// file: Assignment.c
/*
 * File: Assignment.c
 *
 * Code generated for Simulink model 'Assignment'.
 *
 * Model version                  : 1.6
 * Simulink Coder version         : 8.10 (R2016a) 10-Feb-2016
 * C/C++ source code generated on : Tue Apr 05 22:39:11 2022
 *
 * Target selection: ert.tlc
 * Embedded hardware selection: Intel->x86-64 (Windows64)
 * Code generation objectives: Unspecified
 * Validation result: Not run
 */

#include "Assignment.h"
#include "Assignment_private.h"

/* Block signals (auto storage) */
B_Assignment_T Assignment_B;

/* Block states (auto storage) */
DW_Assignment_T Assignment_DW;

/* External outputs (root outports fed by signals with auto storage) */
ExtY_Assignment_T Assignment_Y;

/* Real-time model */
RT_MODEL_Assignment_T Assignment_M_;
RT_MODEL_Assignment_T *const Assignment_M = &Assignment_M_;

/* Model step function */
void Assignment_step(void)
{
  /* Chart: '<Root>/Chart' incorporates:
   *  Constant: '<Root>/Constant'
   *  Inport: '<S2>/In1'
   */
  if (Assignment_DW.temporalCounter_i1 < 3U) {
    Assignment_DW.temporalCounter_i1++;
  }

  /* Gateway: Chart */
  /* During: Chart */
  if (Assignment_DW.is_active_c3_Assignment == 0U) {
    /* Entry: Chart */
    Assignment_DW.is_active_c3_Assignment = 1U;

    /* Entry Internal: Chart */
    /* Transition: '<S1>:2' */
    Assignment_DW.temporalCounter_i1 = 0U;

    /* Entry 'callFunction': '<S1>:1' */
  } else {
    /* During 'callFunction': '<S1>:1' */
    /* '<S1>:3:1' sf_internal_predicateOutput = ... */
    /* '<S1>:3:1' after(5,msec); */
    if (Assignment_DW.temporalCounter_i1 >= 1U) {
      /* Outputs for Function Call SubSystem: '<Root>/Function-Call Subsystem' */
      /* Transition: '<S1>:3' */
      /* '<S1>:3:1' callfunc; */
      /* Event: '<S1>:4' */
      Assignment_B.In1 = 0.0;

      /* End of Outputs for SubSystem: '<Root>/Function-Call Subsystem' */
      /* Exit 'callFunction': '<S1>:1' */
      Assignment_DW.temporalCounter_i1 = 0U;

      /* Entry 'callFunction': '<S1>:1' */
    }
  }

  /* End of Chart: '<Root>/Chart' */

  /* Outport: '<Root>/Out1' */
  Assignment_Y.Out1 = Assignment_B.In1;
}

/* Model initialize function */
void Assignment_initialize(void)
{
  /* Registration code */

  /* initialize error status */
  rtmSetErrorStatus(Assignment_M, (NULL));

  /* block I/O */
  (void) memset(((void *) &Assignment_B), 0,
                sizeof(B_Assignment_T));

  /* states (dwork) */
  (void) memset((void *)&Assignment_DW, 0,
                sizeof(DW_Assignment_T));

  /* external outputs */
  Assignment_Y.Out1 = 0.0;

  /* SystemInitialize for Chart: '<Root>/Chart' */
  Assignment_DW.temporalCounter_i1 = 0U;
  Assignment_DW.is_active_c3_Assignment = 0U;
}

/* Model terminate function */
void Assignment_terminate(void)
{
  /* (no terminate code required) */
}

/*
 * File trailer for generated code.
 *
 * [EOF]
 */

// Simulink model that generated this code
simulink model "Assignment"  (R2016a)
settings: Solver=FixedStepDiscrete  StartTime=0.0  StopTime=inf  RelTol=1e-3

== system Assignment ==
  Chart : Stateflow chart  TreatAsAtomicUnit=on
  Constant : Constant  Value=0
  Function-Call Subsystem : Subsystem  TreatAsAtomicUnit=on
  Lamp : Subsystem  DialogController=hmiCreateDDGDialog  IsWebBlock=on  mask(MWDashboardBlock){webBlockId=50b24cca-d8f1-4ef6-b9f2-5a07ca5c66c6, webBlockType=lamp, ShowInLibBrowser=on, ShowInitialText=on, HMISrcModelName=Assignment}
      mask prompts: webBlockType "WebBlock Type"; HMISrcModelName "Source Model"
  Toggle Switch : Subsystem  DialogController=hmiCreateDDGDialog  IsWebBlock=on  mask(MWDashboardBlock){webBlockId=6b4e1b19-4e30-4abb-a7c7-b79188c6fe27, webBlockType=toggleswitch, ShowInLibBrowser=on, ShowInitialText=on, HMISrcModelName=Assignment}
      mask prompts: webBlockId "WebBlock Id"; webBlockType "WebBlock Type"; HMISrcModelName "Source Model"
  Out1 : Outport
  wires:
  Constant/1 -> Function-Call Subsystem/1(In1)
  Function-Call Subsystem/1(Out1) -> Out1/1
  Chart/1(callfunc()) -> Function-Call Subsystem/Trigger

== system Assignment/Function-Call Subsystem ==
  In1 : Inport
  function : TriggerPort  TriggerType=function-call  VariantControl=Variant
  Out1 : Outport
  wires:
  In1/1 -> Out1/1

== system Assignment/Lamp ==

== system Assignment/Toggle Switch ==

== stateflow chart Assignment/Chart ==
  state callFunction
    en:
    du:
    ex:
  (default) -> callFunction
  callFunction -> callFunction : [after(5,msec)]{callfunc;}
  events: callfunc output FUNCTION_CALL_EVENT
